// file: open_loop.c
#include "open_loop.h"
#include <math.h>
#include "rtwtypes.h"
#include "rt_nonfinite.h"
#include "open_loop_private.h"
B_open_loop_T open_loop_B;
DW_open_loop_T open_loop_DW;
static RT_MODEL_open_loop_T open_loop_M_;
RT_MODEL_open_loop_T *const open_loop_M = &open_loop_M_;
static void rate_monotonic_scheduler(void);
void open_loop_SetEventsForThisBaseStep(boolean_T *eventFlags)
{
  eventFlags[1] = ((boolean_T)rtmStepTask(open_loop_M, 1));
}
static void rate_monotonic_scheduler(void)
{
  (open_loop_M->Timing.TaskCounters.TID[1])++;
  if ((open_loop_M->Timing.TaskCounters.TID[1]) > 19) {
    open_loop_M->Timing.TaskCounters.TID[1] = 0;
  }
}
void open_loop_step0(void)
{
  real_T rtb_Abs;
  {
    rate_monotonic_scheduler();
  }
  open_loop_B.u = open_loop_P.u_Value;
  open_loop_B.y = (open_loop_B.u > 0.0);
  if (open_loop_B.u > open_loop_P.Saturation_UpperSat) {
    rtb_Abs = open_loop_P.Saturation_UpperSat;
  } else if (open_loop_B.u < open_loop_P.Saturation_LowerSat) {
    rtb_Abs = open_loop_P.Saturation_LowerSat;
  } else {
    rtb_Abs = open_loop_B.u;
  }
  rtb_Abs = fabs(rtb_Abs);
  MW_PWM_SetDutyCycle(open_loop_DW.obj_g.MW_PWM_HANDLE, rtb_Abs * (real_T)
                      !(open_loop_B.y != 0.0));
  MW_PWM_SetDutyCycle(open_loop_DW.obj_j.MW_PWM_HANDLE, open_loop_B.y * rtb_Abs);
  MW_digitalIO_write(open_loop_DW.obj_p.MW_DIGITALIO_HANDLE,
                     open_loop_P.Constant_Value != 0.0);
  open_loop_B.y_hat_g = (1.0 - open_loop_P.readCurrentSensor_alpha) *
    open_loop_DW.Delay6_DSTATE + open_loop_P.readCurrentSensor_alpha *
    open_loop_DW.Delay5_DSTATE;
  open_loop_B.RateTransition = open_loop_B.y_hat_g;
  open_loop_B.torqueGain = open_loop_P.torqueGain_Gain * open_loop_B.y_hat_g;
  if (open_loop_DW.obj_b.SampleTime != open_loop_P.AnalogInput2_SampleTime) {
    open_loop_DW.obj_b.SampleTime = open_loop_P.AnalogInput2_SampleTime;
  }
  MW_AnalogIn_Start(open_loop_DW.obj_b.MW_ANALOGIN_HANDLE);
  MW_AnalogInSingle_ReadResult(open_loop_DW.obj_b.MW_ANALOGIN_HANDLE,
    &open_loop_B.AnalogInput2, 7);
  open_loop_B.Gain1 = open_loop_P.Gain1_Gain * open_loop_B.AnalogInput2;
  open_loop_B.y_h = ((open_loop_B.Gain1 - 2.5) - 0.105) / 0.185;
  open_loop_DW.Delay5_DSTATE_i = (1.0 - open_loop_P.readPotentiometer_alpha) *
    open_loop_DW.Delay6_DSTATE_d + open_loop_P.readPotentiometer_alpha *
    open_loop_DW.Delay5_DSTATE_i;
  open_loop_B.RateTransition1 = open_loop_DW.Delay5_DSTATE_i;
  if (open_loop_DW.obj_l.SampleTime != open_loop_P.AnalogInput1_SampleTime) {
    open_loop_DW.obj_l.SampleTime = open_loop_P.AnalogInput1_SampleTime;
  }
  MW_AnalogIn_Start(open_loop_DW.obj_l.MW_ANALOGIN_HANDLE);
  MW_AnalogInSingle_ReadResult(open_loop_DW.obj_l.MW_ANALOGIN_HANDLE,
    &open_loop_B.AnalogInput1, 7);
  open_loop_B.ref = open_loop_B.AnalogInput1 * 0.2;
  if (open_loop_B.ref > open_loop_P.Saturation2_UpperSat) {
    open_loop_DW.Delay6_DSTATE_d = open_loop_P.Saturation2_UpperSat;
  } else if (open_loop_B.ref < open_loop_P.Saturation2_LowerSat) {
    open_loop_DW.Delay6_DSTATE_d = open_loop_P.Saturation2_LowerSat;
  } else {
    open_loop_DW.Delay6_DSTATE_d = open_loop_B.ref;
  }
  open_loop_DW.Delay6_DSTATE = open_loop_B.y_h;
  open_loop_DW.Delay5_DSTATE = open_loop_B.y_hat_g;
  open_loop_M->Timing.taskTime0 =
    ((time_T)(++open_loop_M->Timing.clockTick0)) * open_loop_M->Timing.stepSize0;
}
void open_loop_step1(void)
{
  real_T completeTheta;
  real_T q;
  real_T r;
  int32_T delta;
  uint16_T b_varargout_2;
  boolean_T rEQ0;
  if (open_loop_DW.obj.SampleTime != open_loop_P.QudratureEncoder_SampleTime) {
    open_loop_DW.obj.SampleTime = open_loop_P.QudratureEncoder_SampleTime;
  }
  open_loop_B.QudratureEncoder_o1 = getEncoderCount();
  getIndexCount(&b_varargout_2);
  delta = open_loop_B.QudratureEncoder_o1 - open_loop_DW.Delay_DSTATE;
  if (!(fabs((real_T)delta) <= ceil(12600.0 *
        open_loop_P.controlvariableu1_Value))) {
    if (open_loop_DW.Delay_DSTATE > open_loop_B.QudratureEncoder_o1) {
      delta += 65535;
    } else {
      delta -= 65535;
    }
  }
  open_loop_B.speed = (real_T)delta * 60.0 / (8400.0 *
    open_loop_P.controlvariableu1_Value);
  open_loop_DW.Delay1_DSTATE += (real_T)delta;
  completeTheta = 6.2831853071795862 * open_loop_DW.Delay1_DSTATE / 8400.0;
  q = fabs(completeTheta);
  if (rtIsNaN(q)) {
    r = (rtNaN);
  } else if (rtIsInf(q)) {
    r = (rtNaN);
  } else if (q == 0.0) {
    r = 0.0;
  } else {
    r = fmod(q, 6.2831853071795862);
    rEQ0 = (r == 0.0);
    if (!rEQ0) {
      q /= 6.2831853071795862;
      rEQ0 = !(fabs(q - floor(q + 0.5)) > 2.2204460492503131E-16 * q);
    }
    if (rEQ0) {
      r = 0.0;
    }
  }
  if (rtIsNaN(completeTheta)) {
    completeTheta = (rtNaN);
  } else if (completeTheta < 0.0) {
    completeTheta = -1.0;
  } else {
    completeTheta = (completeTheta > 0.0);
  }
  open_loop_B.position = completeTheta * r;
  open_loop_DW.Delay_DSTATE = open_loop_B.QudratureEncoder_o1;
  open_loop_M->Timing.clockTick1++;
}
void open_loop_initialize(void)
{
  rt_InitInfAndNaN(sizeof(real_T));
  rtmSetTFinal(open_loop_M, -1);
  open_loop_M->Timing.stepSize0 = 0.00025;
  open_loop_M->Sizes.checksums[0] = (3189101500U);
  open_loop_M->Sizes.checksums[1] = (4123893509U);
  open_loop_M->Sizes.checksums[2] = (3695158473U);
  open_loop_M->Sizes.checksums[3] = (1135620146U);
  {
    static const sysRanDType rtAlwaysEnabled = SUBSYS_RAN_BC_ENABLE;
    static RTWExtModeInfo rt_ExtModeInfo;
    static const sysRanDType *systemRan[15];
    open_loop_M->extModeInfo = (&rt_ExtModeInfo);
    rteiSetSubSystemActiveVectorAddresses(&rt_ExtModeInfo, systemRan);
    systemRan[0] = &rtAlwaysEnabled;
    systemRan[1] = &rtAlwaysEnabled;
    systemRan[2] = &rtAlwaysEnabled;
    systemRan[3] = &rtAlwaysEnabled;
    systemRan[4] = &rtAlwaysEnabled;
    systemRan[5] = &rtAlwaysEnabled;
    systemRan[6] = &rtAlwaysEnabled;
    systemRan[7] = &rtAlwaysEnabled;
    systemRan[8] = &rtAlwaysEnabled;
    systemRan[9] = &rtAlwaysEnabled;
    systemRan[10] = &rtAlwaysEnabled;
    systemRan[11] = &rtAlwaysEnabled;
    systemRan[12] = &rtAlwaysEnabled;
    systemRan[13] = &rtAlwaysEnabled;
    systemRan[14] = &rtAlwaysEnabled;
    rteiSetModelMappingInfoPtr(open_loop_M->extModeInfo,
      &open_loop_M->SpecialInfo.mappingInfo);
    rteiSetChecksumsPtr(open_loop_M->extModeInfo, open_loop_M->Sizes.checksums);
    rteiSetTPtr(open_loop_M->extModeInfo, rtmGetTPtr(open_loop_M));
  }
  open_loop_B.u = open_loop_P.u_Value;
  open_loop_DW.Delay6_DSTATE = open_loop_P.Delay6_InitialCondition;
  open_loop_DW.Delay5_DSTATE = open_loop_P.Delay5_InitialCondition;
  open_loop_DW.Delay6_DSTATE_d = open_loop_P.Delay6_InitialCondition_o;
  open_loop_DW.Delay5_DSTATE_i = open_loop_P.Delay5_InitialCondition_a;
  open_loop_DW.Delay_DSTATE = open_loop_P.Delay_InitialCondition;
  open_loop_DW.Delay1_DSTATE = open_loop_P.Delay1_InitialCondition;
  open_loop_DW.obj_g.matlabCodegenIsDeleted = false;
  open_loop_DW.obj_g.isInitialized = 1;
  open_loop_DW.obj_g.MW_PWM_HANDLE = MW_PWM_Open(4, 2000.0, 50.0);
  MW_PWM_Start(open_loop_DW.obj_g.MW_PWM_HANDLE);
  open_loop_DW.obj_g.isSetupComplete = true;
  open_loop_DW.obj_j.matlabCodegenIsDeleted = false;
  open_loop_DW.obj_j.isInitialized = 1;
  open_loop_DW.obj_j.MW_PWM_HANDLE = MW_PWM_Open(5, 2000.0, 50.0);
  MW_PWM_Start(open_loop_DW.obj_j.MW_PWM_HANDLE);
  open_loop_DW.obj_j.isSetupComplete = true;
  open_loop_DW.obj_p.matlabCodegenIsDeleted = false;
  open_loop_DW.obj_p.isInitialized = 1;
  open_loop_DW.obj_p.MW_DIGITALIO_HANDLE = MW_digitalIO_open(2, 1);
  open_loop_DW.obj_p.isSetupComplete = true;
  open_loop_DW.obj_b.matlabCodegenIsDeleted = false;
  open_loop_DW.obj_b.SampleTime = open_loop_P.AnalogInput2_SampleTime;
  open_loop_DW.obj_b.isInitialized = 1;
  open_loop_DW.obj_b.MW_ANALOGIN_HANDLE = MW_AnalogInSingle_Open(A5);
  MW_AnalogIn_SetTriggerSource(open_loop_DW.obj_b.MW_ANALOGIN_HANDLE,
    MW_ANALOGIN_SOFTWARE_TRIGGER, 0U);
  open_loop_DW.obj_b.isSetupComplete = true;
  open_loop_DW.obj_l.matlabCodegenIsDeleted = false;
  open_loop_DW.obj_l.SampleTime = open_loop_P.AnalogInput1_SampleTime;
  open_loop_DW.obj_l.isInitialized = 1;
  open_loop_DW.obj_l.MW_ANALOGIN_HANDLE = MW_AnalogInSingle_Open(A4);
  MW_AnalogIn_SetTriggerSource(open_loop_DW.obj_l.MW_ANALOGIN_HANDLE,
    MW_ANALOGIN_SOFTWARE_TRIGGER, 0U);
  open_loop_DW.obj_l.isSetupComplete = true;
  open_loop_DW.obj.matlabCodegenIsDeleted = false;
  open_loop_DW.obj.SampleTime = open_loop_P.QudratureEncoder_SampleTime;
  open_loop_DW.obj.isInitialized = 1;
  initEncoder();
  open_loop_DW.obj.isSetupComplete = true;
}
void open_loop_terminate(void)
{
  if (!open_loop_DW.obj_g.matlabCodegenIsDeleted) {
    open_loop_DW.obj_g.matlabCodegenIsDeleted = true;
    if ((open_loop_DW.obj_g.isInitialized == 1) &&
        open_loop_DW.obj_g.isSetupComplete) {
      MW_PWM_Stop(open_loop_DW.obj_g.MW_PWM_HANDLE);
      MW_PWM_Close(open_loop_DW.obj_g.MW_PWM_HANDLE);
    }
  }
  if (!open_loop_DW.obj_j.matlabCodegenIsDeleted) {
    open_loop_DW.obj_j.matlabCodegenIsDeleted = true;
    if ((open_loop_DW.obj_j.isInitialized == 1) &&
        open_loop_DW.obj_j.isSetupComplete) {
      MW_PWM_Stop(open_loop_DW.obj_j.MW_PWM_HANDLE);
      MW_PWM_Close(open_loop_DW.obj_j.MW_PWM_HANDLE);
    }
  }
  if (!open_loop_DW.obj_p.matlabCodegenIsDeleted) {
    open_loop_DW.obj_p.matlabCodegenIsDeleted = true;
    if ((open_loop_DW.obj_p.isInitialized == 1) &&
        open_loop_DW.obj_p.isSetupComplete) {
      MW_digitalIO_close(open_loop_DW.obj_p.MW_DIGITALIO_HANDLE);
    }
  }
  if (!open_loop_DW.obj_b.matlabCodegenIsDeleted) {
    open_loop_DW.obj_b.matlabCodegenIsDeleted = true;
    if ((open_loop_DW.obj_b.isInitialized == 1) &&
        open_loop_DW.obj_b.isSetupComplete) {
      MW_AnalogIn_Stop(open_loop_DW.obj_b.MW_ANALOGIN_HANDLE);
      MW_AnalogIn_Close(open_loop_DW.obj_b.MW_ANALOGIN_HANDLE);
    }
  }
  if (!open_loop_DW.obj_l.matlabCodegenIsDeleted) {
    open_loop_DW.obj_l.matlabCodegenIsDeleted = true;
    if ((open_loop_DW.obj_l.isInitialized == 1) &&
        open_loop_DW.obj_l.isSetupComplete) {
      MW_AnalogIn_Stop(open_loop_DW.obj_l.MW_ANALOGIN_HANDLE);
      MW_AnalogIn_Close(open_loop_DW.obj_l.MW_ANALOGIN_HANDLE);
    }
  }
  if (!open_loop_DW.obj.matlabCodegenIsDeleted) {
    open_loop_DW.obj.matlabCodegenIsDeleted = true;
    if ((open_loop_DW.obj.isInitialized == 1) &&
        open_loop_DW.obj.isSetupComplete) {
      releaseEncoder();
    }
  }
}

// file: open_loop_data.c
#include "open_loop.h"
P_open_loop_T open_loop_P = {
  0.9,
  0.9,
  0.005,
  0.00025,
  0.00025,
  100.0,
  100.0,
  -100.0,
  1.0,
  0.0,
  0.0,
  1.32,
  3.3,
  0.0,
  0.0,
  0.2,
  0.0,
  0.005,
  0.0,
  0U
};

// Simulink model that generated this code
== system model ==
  PWMOutput#1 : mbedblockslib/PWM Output  <- 1: Product#1
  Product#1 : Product  <- 1: Abs, 2: Logic#1
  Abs : Abs  <- 1: Saturation
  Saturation : Saturate  UpperLimit=100  LowerLimit=-100  <- 1: Constant#1
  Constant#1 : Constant  Value=100
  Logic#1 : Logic  Operator=NOT  <- 1: MATLABFunction#1
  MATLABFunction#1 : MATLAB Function  <- 1: Constant#1
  PWMOutput#2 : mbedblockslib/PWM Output  <- 1: Product#2
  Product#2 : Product  <- 1: MATLABFunction#1, 2: Abs
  DigitalWrite#1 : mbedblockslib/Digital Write  <- 1: Constant
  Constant : Constant
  RateTransition : RateTransition  <- 1: MATLABFunction#2
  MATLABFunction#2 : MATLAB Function  <- 1: Delay6, 2: Delay5, 3: Constant#2
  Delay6 : Delay  DelayLength=1  InitialCondition=0  <- 1: MATLABFunction#3
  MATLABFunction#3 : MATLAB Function  <- 1: Gain1
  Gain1 : Gain  Gain=3.3  <- 1: AnalogInput2
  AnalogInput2 : mbedblockslib/Analog Input
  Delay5 : Delay  DelayLength=1  InitialCondition=0  <- 1: MATLABFunction#2
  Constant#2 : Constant  Value=alpha
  torqueGain : Gain  Gain=1.32  <- 1: MATLABFunction#2
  RateTransition1 : RateTransition  <- 1: MATLABFunction#4
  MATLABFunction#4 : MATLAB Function  <- 1: Delay#1, 2: Delay#2, 3: Constant#3
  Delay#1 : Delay  DelayLength=1  InitialCondition=0  <- 1: Saturation2
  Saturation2 : Saturate  UpperLimit=0.2  LowerLimit=0  <- 1: MATLABFunction#5
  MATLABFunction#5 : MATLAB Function  <- 1: AnalogInput1
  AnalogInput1 : mbedblockslib/Analog Input
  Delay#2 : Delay  DelayLength=1  InitialCondition=0  <- 1: MATLABFunction#4
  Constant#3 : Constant  Value=alpha
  MATLABFunction#6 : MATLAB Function  <- 1: MATLABFunction#7, 2: controlvariableu1
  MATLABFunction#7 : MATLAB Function  <- 1: QudratureEncoder, 2: Delay, 3: controlvariableu1
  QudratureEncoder : stm_qeplib/Qudrature Encoder
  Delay : Delay  DelayLength=1  InitialCondition=0  <- 1: QudratureEncoder
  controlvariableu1 : Constant  Value=0.005
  MATLABFunction#8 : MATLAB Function  <- 1: Delay1, 2: MATLABFunction#7
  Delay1 : Delay  DelayLength=1  InitialCondition=0  <- 1: MATLABFunction#8/2
== matlab function MATLABFunction#7 ==
function delta = getTicksDelta(currentTicks,lastTicks, Ts)

currentTicks=double(currentTicks);
lastTicks=double(lastTicks);

if abs(currentTicks -lastTicks) <= ceil(12600*Ts)
    delta= currentTicks - lastTicks;
else
    if lastTicks > currentTicks
        delta= currentTicks + 2^16 -1 - lastTicks;
    else
        delta= currentTicks - 2^16 +1 - lastTicks;
    end
end

end

== matlab function MATLABFunction#1 ==
function y = sign(u)
if u >0
    y=1;
else
   y=0;
end

== matlab function MATLABFunction#6 ==
function speed=getSpeedDelta(delta,Ts)
speed=delta * 60/ (8400*Ts);
end

== matlab function MATLABFunction#8 ==
function [position,ticks_star] = getPosition(ticks_star, delta)
    ticks_star=double(ticks_star + delta);
    completeTheta=2*pi*ticks_star/(8400);
    position=sign(completeTheta)*mod(abs(completeTheta), 2*pi)
end

== matlab function firstOrderLagFilter ==
function y_hat = firstOrderLagFilter(y_old, y_hat_old, alpha)
    y_hat= (alpha *y_hat_old) + ((1-alpha)* y_old)
end

== matlab function MATLABFunction#3 ==
function y = readCurrent(u)

y=(u-2.5-0.105)/0.185

== matlab function firstOrderLagFilter ==
function y_hat = firstOrderLagFilter(y_old, y_hat_old, alpha)
    y_hat= (alpha *y_hat_old) + ((1-alpha)* y_old)
end

== matlab function MATLABFunction#5 ==
function ref= getRef(currentRef) 
    
    ref = currentRef * 0.2
end
